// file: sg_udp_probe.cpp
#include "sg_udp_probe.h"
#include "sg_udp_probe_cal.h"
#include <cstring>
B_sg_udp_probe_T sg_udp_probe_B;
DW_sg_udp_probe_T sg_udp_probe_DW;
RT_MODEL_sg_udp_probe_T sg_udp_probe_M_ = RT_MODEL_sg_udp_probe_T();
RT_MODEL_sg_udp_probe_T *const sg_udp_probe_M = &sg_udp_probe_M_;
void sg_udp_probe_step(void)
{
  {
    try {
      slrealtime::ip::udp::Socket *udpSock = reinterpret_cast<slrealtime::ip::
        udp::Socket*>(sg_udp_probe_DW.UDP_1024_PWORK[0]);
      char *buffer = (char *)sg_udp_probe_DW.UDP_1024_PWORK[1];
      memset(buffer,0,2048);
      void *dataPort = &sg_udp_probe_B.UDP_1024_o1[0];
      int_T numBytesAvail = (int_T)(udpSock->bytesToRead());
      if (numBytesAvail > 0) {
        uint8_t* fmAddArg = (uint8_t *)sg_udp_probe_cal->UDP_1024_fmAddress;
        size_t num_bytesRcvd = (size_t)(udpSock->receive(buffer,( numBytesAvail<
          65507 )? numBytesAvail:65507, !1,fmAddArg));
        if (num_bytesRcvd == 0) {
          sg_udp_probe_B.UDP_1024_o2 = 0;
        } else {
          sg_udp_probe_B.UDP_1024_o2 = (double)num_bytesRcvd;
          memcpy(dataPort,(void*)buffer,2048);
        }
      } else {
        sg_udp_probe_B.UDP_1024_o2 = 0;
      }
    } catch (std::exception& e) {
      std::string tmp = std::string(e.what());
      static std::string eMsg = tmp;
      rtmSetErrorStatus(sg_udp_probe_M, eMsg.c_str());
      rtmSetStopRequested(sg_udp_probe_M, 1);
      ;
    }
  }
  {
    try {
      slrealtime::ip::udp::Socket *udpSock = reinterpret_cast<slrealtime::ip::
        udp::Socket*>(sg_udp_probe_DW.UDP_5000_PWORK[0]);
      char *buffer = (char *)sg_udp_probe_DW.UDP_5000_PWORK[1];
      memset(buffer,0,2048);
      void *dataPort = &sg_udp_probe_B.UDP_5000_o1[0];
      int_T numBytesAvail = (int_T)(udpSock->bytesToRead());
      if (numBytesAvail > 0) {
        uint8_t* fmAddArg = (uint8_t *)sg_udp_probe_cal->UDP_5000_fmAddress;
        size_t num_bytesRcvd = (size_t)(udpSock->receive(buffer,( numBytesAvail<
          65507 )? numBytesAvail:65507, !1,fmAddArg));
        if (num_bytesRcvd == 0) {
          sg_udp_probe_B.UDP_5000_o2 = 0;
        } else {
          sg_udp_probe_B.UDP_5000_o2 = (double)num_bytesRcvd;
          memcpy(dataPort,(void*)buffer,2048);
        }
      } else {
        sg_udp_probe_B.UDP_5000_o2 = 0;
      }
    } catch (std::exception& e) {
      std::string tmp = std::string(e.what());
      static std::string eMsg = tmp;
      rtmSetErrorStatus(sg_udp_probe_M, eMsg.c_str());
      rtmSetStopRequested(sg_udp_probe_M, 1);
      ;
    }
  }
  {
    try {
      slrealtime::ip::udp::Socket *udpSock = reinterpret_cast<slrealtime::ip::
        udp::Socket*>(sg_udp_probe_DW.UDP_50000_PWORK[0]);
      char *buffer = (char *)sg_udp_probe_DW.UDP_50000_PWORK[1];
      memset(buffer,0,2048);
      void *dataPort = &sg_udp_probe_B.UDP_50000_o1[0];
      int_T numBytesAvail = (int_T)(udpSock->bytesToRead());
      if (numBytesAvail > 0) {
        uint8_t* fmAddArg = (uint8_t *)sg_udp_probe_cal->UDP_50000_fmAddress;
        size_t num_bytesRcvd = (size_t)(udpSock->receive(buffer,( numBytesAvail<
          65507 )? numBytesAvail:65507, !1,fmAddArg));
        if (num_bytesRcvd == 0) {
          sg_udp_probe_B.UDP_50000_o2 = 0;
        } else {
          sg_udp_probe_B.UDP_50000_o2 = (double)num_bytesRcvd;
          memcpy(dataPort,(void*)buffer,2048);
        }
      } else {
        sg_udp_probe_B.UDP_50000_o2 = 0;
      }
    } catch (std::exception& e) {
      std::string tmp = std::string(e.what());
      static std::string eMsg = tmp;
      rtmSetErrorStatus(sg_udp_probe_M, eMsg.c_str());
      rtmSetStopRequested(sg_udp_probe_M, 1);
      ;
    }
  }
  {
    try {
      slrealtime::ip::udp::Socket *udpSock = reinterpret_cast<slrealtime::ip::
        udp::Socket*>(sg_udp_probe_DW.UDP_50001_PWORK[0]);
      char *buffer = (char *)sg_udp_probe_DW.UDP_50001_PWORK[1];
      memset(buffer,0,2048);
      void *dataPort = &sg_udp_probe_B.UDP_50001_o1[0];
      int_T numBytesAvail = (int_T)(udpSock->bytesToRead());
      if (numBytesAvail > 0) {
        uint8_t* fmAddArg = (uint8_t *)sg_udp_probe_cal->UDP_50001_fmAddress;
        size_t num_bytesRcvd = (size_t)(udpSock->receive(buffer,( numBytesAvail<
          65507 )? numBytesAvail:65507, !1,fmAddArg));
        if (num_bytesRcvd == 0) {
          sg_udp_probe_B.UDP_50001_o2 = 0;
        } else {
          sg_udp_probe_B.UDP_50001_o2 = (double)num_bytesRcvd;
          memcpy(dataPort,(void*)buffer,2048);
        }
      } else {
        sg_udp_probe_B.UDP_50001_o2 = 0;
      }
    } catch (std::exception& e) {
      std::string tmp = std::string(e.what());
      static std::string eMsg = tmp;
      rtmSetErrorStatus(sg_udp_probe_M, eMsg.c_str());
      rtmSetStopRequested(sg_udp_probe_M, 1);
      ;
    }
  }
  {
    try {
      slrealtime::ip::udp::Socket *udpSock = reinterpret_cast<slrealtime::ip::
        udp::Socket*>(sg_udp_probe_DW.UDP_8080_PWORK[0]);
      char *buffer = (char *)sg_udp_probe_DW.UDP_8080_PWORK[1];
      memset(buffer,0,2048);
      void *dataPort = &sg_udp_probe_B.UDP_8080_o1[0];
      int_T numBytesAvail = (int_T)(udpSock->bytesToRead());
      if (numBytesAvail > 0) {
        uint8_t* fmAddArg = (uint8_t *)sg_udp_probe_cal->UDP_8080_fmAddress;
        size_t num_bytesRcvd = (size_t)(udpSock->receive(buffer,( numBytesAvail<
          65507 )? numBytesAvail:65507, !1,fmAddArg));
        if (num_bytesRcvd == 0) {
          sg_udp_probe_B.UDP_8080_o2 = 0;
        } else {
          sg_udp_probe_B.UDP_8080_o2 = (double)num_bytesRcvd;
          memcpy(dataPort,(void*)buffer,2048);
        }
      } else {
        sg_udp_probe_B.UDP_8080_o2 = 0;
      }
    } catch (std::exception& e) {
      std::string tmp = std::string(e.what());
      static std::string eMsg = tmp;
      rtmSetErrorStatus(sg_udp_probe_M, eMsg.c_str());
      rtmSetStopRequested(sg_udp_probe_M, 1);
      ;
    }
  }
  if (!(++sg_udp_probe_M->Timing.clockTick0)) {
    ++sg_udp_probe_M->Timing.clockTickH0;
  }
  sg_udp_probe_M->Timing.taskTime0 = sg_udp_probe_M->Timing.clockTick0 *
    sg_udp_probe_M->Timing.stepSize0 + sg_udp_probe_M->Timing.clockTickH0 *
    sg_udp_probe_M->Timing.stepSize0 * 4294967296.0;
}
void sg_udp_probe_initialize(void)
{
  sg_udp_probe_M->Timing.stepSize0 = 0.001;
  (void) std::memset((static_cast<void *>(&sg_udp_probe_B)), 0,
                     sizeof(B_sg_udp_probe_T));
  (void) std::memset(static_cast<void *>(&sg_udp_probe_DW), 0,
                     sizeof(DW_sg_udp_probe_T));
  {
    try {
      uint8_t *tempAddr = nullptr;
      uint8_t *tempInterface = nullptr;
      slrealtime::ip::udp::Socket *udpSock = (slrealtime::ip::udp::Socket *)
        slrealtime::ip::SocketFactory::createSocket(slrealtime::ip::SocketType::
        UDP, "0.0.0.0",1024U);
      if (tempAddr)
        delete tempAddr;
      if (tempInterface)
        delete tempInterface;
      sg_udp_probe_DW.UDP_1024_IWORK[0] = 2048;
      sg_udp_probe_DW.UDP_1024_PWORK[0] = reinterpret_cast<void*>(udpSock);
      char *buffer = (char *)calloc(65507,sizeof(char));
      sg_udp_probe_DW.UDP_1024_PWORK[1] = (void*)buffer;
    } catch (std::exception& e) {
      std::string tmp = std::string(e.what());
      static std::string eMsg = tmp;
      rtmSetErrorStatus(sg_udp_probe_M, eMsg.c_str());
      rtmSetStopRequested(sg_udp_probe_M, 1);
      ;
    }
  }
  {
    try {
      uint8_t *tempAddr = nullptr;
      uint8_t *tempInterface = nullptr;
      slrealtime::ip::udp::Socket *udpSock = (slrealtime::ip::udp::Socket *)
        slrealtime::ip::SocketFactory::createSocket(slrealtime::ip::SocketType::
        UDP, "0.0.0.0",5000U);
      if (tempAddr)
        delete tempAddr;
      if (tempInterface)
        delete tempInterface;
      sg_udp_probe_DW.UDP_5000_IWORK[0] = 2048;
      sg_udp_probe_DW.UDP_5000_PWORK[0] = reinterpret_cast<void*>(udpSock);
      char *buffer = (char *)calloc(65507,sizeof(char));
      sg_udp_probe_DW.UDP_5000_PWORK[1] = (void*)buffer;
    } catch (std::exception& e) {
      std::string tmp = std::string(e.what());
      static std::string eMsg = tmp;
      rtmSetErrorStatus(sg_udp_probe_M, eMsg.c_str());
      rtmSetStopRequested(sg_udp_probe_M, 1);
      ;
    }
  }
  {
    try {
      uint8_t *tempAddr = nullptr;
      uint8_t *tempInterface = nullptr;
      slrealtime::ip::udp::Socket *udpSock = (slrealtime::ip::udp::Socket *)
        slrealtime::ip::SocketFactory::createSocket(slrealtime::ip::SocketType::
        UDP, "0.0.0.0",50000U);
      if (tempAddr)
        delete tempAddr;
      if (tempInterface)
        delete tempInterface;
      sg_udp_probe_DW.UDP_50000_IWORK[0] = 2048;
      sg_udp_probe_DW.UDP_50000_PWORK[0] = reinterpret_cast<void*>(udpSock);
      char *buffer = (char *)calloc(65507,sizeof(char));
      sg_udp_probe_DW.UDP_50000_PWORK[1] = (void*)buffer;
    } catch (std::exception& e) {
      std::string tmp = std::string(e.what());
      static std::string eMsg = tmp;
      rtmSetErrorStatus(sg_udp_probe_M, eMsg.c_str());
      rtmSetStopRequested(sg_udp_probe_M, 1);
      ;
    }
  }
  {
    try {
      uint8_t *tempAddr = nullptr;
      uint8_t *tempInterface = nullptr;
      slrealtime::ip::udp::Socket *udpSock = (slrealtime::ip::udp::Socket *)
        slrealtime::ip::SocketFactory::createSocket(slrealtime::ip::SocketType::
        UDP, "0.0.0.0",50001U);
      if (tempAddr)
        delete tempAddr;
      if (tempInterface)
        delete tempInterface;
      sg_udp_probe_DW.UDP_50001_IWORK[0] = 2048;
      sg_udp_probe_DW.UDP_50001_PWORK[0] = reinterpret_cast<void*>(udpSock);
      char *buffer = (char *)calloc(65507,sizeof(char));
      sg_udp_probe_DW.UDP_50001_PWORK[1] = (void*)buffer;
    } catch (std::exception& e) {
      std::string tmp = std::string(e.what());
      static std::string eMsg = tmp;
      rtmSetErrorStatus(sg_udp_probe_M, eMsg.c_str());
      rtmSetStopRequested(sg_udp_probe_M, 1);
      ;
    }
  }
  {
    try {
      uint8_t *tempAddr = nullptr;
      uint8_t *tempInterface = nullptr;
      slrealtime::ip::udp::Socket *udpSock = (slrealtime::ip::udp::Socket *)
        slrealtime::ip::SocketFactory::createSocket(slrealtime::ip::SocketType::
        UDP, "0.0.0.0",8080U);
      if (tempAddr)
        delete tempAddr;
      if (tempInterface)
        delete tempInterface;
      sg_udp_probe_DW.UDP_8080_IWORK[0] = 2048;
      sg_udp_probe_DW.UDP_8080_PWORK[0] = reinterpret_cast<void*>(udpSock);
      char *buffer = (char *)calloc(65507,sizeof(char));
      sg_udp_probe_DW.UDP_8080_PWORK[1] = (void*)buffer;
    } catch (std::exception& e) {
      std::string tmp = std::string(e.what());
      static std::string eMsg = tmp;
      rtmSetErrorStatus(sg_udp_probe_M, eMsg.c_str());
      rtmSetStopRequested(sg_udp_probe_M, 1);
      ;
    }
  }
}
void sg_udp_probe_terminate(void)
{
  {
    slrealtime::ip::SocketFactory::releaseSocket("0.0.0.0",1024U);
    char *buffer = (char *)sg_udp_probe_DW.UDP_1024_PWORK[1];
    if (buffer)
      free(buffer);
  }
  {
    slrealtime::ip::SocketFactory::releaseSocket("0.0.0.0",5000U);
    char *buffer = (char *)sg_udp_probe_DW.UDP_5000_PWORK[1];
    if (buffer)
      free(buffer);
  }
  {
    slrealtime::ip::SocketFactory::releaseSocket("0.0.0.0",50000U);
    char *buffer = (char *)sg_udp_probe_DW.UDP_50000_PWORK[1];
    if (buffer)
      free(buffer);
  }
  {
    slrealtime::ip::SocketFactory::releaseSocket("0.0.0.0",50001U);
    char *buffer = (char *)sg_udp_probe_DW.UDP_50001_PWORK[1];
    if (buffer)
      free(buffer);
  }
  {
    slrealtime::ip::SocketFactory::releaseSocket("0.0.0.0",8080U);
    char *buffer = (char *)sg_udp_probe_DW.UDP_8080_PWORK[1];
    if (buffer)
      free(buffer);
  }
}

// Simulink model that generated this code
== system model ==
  UDP_1024 : slrealtimeiplib/UDP Receive
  UDP_5000 : slrealtimeiplib/UDP Receive
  UDP_50000 : slrealtimeiplib/UDP Receive
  UDP_50001 : slrealtimeiplib/UDP Receive
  UDP_8080 : slrealtimeiplib/UDP Receive
